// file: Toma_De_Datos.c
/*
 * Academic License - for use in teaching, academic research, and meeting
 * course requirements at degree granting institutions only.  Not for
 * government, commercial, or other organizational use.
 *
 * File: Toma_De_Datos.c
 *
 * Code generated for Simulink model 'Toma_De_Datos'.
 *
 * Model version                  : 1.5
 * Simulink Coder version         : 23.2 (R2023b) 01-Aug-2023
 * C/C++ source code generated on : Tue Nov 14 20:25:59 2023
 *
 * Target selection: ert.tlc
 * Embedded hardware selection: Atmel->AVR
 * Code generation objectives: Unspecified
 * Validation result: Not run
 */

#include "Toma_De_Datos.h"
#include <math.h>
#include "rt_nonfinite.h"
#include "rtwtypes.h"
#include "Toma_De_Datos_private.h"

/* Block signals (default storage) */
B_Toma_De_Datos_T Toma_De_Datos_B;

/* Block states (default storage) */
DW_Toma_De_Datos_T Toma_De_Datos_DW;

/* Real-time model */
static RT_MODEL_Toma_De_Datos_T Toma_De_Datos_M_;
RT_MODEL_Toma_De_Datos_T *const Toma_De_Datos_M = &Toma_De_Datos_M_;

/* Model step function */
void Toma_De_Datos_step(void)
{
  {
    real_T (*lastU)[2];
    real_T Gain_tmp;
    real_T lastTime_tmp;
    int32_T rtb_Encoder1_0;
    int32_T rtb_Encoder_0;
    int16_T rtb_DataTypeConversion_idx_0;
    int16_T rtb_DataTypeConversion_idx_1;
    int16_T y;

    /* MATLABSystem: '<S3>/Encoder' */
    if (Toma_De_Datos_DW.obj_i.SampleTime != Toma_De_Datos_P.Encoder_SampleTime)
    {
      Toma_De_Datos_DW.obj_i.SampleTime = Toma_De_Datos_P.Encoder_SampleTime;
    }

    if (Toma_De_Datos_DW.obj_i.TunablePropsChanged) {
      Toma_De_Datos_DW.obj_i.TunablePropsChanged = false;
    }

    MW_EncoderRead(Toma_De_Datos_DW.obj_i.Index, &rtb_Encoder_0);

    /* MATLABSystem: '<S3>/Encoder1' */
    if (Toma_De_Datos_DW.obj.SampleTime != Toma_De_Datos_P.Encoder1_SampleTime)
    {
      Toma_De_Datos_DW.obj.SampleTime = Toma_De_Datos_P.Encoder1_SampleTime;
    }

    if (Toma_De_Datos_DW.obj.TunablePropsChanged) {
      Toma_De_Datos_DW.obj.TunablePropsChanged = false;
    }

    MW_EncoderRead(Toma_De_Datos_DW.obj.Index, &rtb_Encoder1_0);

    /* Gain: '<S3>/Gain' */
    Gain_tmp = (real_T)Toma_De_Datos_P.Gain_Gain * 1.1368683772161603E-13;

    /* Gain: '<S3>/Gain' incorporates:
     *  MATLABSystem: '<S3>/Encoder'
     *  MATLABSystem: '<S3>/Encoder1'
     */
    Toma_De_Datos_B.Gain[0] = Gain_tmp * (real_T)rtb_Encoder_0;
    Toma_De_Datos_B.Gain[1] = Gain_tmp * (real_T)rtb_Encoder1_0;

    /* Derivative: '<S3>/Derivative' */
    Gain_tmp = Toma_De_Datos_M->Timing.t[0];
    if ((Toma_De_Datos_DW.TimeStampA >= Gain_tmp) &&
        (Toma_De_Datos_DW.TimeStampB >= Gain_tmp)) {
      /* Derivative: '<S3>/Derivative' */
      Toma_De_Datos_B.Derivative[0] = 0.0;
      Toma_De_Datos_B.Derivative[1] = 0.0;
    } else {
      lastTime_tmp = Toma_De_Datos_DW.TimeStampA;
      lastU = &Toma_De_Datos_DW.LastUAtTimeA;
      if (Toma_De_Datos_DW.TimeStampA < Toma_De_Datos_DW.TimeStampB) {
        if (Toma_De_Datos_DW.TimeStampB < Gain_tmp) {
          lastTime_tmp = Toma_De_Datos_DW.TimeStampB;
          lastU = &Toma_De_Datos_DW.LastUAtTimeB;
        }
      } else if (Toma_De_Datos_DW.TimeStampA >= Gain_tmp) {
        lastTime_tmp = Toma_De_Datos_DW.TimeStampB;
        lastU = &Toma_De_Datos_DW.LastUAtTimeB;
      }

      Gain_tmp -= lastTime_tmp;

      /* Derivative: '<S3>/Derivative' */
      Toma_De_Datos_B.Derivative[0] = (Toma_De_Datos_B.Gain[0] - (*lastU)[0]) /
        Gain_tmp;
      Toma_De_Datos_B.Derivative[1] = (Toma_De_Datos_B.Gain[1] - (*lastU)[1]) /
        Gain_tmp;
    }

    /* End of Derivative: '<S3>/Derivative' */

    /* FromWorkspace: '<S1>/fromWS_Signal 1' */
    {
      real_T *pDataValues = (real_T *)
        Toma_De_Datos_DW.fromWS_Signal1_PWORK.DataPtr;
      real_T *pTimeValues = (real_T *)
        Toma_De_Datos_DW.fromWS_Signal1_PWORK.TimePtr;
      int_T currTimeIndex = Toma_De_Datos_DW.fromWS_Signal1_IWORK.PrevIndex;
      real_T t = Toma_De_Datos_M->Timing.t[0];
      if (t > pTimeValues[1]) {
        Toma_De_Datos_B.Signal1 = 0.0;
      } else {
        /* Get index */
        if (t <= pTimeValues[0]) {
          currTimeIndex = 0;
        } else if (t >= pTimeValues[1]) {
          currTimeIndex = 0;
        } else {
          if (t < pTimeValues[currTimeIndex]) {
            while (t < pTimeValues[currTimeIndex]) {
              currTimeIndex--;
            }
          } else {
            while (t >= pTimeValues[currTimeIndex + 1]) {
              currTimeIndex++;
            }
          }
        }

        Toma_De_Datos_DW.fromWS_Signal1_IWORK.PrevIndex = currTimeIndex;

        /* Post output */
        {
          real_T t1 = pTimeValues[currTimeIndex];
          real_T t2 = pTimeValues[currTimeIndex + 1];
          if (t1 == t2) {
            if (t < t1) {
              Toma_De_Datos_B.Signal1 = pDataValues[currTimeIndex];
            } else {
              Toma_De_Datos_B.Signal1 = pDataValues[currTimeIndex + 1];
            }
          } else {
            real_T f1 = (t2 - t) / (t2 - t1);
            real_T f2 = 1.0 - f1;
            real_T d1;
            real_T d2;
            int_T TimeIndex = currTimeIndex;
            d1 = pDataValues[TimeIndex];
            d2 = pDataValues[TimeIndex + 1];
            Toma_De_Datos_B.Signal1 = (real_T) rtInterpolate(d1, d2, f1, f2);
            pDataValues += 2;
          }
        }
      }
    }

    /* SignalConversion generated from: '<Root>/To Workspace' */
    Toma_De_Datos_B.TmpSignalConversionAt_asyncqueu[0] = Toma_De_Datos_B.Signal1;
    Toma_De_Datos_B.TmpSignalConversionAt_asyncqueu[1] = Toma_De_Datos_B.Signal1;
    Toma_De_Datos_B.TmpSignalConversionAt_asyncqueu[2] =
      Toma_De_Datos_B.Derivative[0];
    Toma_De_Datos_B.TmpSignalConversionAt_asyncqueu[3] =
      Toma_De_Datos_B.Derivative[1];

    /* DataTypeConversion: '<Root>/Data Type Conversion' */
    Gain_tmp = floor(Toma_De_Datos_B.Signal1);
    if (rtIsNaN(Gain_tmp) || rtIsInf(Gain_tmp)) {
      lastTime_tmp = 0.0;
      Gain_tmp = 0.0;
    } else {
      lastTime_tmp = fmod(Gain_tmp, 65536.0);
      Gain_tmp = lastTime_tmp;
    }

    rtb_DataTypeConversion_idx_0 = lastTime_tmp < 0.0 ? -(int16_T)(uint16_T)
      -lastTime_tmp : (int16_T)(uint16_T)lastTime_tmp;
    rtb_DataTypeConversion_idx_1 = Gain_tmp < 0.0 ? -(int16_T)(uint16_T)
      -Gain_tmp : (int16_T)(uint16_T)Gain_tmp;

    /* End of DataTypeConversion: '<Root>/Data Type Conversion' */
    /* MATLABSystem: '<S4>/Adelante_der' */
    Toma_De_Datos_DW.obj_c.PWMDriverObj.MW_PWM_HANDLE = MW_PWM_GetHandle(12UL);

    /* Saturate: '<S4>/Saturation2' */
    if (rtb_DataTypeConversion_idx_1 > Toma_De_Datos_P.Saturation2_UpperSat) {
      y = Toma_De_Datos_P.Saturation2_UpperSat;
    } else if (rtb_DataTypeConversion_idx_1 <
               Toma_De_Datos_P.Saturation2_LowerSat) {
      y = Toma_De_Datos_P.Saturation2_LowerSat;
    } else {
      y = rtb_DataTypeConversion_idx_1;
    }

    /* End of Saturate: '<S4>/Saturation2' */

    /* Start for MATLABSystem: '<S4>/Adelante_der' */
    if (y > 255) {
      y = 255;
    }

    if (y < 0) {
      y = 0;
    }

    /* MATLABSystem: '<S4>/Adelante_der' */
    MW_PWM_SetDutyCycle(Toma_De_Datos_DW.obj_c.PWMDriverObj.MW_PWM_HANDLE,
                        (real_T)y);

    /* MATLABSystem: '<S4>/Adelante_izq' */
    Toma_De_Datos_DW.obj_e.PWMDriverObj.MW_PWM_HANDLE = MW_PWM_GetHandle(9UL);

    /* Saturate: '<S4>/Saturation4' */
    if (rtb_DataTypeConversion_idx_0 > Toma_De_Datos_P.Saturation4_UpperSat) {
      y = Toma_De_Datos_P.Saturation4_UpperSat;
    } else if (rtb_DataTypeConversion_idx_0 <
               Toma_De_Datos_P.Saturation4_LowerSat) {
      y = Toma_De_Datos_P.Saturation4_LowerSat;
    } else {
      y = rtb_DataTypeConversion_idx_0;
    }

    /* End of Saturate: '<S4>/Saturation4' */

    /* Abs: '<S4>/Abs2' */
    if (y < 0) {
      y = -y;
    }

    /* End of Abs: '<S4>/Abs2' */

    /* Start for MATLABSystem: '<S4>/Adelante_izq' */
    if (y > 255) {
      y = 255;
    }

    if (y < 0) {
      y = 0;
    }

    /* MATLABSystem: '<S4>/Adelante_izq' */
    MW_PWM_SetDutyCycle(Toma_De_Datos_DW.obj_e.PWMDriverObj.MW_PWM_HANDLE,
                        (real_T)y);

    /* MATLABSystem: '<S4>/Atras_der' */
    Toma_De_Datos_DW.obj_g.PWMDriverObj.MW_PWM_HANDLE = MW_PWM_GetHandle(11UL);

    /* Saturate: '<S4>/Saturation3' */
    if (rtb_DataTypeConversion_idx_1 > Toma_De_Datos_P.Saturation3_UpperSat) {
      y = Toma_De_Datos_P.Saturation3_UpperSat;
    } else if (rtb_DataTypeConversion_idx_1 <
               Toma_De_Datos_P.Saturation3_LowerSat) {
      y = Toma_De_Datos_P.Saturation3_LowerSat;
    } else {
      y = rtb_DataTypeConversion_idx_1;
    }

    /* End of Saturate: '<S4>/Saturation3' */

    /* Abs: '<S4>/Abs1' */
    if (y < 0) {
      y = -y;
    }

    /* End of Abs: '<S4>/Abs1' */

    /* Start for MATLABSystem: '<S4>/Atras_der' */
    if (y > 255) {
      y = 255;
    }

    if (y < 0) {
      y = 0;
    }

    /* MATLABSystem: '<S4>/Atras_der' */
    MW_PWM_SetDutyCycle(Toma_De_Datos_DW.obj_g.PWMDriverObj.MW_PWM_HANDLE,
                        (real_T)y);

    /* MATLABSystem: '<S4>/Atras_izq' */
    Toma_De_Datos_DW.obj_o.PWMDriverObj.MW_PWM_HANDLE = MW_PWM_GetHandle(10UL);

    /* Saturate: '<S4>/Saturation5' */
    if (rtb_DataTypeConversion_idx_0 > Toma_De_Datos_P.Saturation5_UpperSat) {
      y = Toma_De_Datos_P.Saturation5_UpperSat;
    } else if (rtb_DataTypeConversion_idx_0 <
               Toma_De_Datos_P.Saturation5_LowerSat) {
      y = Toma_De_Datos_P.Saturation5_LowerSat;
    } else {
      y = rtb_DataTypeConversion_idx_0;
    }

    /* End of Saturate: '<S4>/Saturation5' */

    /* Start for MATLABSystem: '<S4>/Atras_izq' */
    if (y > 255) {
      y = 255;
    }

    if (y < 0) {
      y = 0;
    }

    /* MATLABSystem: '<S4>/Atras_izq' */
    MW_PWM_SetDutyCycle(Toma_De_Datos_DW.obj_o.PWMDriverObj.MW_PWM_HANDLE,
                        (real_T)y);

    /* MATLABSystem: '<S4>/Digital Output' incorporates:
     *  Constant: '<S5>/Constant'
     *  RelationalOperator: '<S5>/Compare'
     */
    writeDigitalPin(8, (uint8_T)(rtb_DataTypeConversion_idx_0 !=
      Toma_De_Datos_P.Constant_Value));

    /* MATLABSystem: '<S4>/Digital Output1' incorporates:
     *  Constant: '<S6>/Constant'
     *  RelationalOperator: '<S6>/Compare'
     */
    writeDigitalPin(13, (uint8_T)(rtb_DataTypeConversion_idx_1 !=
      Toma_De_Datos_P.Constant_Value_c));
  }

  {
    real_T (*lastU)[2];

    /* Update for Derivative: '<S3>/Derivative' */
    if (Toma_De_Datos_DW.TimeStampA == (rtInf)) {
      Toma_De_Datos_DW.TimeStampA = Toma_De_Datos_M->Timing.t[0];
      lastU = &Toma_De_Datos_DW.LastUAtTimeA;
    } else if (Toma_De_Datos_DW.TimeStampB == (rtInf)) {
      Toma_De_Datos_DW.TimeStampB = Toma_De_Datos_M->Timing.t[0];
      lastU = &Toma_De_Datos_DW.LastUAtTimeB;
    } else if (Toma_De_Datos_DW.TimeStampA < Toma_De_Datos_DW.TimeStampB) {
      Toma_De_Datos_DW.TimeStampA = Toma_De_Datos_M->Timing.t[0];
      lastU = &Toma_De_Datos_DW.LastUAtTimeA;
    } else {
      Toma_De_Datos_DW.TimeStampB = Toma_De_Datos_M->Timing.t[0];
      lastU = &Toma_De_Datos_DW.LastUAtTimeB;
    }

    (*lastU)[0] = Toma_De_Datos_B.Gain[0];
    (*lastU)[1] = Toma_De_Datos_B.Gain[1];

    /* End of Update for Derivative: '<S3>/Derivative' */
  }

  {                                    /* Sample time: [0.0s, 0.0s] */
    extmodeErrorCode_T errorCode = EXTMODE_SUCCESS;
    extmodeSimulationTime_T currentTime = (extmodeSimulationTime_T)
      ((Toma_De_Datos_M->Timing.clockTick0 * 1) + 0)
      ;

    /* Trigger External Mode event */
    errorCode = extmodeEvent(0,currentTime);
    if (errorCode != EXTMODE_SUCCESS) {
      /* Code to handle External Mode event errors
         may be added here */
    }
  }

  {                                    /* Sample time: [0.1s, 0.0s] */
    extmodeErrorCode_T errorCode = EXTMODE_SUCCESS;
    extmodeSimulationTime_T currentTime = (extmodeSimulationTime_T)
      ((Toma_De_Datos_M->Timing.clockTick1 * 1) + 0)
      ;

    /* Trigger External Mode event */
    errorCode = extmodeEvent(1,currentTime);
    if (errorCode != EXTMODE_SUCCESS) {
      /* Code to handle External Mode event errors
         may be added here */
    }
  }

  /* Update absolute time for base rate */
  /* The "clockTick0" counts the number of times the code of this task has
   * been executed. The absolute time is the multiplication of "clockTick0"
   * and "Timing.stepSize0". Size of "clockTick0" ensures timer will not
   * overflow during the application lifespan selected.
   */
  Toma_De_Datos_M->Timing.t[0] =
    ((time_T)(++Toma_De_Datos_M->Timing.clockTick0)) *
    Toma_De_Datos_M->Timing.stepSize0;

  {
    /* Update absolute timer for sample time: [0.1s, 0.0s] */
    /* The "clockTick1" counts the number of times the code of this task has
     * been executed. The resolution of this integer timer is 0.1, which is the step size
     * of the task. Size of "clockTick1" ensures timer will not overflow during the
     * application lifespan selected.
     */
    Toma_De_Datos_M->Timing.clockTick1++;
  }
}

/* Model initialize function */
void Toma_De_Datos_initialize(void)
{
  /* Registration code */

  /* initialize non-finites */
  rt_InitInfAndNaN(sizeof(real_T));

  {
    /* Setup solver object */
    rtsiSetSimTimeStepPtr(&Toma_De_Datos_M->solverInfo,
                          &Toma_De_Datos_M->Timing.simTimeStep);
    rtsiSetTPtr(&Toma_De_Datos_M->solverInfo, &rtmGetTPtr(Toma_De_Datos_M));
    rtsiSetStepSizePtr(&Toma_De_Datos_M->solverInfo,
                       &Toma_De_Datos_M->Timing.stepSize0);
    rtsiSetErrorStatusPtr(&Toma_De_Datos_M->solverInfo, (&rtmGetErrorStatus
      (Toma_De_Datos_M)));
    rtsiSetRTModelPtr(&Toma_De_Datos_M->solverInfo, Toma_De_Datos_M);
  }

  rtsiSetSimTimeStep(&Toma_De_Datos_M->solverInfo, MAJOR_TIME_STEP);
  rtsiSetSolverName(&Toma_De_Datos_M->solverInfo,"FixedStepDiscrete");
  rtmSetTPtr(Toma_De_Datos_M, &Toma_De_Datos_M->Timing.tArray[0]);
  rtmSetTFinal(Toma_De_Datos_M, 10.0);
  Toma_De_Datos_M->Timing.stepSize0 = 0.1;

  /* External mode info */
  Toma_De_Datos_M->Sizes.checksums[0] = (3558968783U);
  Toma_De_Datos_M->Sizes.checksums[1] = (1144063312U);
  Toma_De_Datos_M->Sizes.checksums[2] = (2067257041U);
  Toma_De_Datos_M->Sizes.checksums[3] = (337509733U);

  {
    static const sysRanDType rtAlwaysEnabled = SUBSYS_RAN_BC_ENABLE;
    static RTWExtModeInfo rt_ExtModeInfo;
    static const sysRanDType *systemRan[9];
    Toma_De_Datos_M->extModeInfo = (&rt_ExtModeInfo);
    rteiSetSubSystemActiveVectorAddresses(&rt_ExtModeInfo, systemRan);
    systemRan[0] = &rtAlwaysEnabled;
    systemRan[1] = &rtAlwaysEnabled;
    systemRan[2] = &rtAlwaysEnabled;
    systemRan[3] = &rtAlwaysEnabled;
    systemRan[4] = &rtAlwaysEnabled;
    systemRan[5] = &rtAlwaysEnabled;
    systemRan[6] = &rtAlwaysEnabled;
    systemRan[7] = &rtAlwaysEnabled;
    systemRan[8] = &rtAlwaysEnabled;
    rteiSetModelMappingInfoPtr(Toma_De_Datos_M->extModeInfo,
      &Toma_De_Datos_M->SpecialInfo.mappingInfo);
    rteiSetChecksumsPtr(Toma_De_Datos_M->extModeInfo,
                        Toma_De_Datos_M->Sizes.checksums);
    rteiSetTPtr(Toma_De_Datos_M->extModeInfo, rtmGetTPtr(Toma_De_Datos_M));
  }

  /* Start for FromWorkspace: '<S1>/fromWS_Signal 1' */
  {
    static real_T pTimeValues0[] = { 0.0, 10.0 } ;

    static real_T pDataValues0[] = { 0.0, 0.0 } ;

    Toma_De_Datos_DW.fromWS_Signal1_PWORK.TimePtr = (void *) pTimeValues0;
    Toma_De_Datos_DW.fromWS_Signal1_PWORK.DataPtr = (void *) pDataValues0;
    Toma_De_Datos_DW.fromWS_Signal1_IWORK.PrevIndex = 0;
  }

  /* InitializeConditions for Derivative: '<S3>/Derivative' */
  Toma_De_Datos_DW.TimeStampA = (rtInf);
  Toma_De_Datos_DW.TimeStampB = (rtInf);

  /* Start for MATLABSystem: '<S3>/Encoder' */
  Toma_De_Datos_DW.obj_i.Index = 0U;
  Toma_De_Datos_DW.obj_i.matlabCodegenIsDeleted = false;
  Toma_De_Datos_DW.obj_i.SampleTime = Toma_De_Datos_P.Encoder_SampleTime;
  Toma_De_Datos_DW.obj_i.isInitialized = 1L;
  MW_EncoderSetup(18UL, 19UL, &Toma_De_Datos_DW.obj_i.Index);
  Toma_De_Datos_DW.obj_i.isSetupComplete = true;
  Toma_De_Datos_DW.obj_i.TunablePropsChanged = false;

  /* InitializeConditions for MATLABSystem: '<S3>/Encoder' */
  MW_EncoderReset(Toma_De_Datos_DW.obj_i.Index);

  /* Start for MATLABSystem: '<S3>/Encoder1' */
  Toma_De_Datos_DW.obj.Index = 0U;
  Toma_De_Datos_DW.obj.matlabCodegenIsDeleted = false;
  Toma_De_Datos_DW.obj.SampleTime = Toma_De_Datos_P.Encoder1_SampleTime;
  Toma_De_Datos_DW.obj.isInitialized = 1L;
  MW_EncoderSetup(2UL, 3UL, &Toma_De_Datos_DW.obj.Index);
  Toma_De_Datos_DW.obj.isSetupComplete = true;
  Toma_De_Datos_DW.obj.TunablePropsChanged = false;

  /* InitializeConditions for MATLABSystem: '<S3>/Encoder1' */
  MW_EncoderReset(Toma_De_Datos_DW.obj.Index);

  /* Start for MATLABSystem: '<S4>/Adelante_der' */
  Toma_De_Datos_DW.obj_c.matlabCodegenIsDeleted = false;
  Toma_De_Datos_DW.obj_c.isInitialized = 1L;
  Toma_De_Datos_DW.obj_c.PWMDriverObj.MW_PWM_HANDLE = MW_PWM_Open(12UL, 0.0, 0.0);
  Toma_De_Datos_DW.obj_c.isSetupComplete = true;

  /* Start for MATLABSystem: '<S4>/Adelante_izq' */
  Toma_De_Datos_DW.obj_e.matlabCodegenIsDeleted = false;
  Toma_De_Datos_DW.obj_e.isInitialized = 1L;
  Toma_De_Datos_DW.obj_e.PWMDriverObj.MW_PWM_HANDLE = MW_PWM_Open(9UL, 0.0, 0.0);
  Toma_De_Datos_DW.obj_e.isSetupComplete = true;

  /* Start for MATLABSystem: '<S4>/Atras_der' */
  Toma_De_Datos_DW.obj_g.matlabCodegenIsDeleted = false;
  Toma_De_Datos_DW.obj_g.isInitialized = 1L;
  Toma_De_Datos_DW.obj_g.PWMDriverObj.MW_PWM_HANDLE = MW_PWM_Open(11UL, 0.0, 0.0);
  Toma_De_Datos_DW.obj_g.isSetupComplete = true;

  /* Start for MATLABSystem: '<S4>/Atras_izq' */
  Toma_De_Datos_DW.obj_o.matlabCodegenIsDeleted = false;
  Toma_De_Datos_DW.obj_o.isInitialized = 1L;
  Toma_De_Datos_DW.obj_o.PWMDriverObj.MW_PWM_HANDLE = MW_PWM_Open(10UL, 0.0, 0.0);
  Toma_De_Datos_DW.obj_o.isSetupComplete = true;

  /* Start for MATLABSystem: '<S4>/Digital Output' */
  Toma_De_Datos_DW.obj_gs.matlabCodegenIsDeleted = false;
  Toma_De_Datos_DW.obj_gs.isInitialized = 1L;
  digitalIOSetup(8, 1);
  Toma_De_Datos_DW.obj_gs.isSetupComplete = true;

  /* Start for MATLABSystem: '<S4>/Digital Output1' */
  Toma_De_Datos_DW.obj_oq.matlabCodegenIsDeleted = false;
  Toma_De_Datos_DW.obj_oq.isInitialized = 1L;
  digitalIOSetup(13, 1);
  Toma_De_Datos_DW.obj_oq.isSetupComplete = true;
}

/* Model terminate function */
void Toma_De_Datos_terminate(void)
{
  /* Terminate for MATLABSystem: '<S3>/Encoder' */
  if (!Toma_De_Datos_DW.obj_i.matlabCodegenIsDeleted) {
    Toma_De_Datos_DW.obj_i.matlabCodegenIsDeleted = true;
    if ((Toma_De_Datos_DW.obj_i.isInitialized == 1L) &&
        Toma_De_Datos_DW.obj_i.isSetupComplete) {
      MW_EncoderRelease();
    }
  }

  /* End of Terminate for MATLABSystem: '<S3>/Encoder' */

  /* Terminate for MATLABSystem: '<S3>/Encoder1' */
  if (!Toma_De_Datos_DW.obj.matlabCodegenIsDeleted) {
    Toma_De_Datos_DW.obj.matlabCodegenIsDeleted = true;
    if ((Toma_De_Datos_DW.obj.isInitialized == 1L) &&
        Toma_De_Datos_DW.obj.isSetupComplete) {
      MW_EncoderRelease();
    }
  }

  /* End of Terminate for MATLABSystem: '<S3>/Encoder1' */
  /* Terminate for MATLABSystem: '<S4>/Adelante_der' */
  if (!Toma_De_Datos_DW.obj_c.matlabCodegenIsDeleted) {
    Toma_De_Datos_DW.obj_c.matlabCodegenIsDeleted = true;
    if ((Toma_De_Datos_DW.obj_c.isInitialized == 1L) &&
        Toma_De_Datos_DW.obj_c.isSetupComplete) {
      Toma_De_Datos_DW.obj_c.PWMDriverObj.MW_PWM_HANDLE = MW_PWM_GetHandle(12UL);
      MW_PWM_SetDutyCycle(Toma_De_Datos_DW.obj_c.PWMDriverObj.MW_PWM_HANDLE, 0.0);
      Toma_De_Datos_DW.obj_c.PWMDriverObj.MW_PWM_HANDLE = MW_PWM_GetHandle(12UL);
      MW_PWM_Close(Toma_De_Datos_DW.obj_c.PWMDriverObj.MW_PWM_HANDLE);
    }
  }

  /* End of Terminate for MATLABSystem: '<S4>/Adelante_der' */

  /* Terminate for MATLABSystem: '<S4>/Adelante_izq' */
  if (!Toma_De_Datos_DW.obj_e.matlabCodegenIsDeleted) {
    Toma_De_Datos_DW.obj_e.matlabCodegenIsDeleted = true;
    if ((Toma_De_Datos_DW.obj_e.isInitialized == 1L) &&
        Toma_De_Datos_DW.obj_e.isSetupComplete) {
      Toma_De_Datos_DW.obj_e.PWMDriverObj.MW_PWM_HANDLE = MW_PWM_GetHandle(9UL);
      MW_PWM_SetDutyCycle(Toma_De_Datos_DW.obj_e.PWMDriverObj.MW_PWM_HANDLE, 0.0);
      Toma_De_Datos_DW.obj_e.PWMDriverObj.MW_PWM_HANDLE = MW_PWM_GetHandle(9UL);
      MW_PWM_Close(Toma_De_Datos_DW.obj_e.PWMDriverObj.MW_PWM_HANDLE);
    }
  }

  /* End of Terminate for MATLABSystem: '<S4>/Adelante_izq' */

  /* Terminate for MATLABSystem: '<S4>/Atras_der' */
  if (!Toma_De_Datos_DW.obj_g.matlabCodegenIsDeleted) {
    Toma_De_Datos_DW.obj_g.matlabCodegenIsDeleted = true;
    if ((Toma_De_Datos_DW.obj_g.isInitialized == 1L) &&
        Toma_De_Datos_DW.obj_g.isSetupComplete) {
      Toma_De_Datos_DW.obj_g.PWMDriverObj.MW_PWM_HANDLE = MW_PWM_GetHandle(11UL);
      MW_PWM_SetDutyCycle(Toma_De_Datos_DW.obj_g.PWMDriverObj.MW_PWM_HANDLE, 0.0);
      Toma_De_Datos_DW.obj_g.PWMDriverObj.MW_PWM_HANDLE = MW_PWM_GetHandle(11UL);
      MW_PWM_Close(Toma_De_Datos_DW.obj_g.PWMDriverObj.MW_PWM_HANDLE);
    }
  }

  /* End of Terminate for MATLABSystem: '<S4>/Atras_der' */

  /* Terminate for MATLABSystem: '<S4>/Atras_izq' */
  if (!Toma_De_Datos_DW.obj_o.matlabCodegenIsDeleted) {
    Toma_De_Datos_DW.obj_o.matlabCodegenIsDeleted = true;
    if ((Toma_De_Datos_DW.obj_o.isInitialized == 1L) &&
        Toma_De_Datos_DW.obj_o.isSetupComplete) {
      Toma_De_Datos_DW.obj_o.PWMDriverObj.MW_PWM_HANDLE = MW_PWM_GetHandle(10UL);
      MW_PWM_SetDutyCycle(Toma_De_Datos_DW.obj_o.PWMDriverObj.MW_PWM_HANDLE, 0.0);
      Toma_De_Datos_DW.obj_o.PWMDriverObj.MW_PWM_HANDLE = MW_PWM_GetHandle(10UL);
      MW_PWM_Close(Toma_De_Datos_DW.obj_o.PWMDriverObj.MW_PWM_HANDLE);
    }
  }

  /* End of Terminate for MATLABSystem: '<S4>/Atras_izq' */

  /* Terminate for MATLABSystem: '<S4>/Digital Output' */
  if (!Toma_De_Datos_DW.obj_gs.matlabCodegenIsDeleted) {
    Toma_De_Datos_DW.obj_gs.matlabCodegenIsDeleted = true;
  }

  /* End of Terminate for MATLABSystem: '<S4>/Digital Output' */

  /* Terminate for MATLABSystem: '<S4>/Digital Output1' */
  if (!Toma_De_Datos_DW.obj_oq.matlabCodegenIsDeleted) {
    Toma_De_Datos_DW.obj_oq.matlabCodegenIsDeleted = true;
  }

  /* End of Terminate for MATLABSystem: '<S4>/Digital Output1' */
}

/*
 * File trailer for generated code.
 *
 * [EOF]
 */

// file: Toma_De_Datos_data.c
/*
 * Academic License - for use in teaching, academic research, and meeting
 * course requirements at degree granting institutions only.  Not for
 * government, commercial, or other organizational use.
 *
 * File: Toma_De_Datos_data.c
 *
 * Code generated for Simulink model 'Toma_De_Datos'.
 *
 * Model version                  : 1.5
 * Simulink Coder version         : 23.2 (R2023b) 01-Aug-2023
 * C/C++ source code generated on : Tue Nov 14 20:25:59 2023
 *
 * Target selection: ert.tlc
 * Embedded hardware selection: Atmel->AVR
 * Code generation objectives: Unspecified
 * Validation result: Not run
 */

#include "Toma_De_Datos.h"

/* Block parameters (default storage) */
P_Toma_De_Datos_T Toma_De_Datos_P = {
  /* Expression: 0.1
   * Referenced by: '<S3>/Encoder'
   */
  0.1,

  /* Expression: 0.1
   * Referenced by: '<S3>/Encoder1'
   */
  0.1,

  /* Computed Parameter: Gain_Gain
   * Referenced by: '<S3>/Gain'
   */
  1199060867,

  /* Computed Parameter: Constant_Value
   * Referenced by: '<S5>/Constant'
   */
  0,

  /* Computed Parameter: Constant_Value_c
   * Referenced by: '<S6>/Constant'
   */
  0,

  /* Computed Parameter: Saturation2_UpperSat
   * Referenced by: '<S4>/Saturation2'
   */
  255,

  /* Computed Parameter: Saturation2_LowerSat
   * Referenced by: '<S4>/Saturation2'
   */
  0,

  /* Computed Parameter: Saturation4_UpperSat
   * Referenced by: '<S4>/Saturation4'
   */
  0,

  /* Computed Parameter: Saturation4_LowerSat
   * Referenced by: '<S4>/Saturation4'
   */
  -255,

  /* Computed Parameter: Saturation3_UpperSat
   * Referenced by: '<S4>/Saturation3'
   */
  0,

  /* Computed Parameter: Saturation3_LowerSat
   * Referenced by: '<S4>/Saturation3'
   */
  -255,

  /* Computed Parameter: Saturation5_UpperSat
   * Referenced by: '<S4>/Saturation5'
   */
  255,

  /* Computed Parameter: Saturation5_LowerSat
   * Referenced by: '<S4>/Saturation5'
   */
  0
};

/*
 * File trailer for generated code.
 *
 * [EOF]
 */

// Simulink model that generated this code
simulink model "Toma_De_Datos"  (R2023b)
settings: Solver=FixedStepAuto  StartTime=0.0  StopTime=10  RelTol=1e-3  EnableMultiTasking=on
libraries: SignalEditorBlockLib x1

== system Toma_De_Datos ==
  Data Type Conversion : DataTypeConversion  OutDataTypeStr=int16  SaturateOnIntegerOverflow=off  RndMeth=Floor
  Mux : Mux  Inputs=2
  Mux1 : Mux  Inputs=2
  Scope : Scope  NumInputPorts=2
  Signal Editor : SignalEditorBlockLib/Signal Editor  FileName=Señal_PWM.mat  ActiveScenario=PWM  ActiveSignal=PWM  IsBus=off  OutputBusObjectStr=Bus: BusObject  SampleTime=0  OutputAfterFinalValue=Setting to zero  Unit=inherit  PreserveSignalName=on  ApplySigPropsToAllScenarios=on  ApplySigPropsToAllSignals=off
  Subsystem Reference : Subsystem  ReferencedSubsystem=Piero_Hardware
  To Workspace : ToWorkspace  VariableName=simout  SampleTime=-1
  wires:
  Signal Editor/1 -> Scope/2, Mux/1, Mux/2
  Mux/1 -> Mux1/1, Data Type Conversion/1
  Data Type Conversion/1 -> Subsystem Reference/1
  Subsystem Reference/1 -> Mux1/2
  Mux1/1 -> To Workspace/1
